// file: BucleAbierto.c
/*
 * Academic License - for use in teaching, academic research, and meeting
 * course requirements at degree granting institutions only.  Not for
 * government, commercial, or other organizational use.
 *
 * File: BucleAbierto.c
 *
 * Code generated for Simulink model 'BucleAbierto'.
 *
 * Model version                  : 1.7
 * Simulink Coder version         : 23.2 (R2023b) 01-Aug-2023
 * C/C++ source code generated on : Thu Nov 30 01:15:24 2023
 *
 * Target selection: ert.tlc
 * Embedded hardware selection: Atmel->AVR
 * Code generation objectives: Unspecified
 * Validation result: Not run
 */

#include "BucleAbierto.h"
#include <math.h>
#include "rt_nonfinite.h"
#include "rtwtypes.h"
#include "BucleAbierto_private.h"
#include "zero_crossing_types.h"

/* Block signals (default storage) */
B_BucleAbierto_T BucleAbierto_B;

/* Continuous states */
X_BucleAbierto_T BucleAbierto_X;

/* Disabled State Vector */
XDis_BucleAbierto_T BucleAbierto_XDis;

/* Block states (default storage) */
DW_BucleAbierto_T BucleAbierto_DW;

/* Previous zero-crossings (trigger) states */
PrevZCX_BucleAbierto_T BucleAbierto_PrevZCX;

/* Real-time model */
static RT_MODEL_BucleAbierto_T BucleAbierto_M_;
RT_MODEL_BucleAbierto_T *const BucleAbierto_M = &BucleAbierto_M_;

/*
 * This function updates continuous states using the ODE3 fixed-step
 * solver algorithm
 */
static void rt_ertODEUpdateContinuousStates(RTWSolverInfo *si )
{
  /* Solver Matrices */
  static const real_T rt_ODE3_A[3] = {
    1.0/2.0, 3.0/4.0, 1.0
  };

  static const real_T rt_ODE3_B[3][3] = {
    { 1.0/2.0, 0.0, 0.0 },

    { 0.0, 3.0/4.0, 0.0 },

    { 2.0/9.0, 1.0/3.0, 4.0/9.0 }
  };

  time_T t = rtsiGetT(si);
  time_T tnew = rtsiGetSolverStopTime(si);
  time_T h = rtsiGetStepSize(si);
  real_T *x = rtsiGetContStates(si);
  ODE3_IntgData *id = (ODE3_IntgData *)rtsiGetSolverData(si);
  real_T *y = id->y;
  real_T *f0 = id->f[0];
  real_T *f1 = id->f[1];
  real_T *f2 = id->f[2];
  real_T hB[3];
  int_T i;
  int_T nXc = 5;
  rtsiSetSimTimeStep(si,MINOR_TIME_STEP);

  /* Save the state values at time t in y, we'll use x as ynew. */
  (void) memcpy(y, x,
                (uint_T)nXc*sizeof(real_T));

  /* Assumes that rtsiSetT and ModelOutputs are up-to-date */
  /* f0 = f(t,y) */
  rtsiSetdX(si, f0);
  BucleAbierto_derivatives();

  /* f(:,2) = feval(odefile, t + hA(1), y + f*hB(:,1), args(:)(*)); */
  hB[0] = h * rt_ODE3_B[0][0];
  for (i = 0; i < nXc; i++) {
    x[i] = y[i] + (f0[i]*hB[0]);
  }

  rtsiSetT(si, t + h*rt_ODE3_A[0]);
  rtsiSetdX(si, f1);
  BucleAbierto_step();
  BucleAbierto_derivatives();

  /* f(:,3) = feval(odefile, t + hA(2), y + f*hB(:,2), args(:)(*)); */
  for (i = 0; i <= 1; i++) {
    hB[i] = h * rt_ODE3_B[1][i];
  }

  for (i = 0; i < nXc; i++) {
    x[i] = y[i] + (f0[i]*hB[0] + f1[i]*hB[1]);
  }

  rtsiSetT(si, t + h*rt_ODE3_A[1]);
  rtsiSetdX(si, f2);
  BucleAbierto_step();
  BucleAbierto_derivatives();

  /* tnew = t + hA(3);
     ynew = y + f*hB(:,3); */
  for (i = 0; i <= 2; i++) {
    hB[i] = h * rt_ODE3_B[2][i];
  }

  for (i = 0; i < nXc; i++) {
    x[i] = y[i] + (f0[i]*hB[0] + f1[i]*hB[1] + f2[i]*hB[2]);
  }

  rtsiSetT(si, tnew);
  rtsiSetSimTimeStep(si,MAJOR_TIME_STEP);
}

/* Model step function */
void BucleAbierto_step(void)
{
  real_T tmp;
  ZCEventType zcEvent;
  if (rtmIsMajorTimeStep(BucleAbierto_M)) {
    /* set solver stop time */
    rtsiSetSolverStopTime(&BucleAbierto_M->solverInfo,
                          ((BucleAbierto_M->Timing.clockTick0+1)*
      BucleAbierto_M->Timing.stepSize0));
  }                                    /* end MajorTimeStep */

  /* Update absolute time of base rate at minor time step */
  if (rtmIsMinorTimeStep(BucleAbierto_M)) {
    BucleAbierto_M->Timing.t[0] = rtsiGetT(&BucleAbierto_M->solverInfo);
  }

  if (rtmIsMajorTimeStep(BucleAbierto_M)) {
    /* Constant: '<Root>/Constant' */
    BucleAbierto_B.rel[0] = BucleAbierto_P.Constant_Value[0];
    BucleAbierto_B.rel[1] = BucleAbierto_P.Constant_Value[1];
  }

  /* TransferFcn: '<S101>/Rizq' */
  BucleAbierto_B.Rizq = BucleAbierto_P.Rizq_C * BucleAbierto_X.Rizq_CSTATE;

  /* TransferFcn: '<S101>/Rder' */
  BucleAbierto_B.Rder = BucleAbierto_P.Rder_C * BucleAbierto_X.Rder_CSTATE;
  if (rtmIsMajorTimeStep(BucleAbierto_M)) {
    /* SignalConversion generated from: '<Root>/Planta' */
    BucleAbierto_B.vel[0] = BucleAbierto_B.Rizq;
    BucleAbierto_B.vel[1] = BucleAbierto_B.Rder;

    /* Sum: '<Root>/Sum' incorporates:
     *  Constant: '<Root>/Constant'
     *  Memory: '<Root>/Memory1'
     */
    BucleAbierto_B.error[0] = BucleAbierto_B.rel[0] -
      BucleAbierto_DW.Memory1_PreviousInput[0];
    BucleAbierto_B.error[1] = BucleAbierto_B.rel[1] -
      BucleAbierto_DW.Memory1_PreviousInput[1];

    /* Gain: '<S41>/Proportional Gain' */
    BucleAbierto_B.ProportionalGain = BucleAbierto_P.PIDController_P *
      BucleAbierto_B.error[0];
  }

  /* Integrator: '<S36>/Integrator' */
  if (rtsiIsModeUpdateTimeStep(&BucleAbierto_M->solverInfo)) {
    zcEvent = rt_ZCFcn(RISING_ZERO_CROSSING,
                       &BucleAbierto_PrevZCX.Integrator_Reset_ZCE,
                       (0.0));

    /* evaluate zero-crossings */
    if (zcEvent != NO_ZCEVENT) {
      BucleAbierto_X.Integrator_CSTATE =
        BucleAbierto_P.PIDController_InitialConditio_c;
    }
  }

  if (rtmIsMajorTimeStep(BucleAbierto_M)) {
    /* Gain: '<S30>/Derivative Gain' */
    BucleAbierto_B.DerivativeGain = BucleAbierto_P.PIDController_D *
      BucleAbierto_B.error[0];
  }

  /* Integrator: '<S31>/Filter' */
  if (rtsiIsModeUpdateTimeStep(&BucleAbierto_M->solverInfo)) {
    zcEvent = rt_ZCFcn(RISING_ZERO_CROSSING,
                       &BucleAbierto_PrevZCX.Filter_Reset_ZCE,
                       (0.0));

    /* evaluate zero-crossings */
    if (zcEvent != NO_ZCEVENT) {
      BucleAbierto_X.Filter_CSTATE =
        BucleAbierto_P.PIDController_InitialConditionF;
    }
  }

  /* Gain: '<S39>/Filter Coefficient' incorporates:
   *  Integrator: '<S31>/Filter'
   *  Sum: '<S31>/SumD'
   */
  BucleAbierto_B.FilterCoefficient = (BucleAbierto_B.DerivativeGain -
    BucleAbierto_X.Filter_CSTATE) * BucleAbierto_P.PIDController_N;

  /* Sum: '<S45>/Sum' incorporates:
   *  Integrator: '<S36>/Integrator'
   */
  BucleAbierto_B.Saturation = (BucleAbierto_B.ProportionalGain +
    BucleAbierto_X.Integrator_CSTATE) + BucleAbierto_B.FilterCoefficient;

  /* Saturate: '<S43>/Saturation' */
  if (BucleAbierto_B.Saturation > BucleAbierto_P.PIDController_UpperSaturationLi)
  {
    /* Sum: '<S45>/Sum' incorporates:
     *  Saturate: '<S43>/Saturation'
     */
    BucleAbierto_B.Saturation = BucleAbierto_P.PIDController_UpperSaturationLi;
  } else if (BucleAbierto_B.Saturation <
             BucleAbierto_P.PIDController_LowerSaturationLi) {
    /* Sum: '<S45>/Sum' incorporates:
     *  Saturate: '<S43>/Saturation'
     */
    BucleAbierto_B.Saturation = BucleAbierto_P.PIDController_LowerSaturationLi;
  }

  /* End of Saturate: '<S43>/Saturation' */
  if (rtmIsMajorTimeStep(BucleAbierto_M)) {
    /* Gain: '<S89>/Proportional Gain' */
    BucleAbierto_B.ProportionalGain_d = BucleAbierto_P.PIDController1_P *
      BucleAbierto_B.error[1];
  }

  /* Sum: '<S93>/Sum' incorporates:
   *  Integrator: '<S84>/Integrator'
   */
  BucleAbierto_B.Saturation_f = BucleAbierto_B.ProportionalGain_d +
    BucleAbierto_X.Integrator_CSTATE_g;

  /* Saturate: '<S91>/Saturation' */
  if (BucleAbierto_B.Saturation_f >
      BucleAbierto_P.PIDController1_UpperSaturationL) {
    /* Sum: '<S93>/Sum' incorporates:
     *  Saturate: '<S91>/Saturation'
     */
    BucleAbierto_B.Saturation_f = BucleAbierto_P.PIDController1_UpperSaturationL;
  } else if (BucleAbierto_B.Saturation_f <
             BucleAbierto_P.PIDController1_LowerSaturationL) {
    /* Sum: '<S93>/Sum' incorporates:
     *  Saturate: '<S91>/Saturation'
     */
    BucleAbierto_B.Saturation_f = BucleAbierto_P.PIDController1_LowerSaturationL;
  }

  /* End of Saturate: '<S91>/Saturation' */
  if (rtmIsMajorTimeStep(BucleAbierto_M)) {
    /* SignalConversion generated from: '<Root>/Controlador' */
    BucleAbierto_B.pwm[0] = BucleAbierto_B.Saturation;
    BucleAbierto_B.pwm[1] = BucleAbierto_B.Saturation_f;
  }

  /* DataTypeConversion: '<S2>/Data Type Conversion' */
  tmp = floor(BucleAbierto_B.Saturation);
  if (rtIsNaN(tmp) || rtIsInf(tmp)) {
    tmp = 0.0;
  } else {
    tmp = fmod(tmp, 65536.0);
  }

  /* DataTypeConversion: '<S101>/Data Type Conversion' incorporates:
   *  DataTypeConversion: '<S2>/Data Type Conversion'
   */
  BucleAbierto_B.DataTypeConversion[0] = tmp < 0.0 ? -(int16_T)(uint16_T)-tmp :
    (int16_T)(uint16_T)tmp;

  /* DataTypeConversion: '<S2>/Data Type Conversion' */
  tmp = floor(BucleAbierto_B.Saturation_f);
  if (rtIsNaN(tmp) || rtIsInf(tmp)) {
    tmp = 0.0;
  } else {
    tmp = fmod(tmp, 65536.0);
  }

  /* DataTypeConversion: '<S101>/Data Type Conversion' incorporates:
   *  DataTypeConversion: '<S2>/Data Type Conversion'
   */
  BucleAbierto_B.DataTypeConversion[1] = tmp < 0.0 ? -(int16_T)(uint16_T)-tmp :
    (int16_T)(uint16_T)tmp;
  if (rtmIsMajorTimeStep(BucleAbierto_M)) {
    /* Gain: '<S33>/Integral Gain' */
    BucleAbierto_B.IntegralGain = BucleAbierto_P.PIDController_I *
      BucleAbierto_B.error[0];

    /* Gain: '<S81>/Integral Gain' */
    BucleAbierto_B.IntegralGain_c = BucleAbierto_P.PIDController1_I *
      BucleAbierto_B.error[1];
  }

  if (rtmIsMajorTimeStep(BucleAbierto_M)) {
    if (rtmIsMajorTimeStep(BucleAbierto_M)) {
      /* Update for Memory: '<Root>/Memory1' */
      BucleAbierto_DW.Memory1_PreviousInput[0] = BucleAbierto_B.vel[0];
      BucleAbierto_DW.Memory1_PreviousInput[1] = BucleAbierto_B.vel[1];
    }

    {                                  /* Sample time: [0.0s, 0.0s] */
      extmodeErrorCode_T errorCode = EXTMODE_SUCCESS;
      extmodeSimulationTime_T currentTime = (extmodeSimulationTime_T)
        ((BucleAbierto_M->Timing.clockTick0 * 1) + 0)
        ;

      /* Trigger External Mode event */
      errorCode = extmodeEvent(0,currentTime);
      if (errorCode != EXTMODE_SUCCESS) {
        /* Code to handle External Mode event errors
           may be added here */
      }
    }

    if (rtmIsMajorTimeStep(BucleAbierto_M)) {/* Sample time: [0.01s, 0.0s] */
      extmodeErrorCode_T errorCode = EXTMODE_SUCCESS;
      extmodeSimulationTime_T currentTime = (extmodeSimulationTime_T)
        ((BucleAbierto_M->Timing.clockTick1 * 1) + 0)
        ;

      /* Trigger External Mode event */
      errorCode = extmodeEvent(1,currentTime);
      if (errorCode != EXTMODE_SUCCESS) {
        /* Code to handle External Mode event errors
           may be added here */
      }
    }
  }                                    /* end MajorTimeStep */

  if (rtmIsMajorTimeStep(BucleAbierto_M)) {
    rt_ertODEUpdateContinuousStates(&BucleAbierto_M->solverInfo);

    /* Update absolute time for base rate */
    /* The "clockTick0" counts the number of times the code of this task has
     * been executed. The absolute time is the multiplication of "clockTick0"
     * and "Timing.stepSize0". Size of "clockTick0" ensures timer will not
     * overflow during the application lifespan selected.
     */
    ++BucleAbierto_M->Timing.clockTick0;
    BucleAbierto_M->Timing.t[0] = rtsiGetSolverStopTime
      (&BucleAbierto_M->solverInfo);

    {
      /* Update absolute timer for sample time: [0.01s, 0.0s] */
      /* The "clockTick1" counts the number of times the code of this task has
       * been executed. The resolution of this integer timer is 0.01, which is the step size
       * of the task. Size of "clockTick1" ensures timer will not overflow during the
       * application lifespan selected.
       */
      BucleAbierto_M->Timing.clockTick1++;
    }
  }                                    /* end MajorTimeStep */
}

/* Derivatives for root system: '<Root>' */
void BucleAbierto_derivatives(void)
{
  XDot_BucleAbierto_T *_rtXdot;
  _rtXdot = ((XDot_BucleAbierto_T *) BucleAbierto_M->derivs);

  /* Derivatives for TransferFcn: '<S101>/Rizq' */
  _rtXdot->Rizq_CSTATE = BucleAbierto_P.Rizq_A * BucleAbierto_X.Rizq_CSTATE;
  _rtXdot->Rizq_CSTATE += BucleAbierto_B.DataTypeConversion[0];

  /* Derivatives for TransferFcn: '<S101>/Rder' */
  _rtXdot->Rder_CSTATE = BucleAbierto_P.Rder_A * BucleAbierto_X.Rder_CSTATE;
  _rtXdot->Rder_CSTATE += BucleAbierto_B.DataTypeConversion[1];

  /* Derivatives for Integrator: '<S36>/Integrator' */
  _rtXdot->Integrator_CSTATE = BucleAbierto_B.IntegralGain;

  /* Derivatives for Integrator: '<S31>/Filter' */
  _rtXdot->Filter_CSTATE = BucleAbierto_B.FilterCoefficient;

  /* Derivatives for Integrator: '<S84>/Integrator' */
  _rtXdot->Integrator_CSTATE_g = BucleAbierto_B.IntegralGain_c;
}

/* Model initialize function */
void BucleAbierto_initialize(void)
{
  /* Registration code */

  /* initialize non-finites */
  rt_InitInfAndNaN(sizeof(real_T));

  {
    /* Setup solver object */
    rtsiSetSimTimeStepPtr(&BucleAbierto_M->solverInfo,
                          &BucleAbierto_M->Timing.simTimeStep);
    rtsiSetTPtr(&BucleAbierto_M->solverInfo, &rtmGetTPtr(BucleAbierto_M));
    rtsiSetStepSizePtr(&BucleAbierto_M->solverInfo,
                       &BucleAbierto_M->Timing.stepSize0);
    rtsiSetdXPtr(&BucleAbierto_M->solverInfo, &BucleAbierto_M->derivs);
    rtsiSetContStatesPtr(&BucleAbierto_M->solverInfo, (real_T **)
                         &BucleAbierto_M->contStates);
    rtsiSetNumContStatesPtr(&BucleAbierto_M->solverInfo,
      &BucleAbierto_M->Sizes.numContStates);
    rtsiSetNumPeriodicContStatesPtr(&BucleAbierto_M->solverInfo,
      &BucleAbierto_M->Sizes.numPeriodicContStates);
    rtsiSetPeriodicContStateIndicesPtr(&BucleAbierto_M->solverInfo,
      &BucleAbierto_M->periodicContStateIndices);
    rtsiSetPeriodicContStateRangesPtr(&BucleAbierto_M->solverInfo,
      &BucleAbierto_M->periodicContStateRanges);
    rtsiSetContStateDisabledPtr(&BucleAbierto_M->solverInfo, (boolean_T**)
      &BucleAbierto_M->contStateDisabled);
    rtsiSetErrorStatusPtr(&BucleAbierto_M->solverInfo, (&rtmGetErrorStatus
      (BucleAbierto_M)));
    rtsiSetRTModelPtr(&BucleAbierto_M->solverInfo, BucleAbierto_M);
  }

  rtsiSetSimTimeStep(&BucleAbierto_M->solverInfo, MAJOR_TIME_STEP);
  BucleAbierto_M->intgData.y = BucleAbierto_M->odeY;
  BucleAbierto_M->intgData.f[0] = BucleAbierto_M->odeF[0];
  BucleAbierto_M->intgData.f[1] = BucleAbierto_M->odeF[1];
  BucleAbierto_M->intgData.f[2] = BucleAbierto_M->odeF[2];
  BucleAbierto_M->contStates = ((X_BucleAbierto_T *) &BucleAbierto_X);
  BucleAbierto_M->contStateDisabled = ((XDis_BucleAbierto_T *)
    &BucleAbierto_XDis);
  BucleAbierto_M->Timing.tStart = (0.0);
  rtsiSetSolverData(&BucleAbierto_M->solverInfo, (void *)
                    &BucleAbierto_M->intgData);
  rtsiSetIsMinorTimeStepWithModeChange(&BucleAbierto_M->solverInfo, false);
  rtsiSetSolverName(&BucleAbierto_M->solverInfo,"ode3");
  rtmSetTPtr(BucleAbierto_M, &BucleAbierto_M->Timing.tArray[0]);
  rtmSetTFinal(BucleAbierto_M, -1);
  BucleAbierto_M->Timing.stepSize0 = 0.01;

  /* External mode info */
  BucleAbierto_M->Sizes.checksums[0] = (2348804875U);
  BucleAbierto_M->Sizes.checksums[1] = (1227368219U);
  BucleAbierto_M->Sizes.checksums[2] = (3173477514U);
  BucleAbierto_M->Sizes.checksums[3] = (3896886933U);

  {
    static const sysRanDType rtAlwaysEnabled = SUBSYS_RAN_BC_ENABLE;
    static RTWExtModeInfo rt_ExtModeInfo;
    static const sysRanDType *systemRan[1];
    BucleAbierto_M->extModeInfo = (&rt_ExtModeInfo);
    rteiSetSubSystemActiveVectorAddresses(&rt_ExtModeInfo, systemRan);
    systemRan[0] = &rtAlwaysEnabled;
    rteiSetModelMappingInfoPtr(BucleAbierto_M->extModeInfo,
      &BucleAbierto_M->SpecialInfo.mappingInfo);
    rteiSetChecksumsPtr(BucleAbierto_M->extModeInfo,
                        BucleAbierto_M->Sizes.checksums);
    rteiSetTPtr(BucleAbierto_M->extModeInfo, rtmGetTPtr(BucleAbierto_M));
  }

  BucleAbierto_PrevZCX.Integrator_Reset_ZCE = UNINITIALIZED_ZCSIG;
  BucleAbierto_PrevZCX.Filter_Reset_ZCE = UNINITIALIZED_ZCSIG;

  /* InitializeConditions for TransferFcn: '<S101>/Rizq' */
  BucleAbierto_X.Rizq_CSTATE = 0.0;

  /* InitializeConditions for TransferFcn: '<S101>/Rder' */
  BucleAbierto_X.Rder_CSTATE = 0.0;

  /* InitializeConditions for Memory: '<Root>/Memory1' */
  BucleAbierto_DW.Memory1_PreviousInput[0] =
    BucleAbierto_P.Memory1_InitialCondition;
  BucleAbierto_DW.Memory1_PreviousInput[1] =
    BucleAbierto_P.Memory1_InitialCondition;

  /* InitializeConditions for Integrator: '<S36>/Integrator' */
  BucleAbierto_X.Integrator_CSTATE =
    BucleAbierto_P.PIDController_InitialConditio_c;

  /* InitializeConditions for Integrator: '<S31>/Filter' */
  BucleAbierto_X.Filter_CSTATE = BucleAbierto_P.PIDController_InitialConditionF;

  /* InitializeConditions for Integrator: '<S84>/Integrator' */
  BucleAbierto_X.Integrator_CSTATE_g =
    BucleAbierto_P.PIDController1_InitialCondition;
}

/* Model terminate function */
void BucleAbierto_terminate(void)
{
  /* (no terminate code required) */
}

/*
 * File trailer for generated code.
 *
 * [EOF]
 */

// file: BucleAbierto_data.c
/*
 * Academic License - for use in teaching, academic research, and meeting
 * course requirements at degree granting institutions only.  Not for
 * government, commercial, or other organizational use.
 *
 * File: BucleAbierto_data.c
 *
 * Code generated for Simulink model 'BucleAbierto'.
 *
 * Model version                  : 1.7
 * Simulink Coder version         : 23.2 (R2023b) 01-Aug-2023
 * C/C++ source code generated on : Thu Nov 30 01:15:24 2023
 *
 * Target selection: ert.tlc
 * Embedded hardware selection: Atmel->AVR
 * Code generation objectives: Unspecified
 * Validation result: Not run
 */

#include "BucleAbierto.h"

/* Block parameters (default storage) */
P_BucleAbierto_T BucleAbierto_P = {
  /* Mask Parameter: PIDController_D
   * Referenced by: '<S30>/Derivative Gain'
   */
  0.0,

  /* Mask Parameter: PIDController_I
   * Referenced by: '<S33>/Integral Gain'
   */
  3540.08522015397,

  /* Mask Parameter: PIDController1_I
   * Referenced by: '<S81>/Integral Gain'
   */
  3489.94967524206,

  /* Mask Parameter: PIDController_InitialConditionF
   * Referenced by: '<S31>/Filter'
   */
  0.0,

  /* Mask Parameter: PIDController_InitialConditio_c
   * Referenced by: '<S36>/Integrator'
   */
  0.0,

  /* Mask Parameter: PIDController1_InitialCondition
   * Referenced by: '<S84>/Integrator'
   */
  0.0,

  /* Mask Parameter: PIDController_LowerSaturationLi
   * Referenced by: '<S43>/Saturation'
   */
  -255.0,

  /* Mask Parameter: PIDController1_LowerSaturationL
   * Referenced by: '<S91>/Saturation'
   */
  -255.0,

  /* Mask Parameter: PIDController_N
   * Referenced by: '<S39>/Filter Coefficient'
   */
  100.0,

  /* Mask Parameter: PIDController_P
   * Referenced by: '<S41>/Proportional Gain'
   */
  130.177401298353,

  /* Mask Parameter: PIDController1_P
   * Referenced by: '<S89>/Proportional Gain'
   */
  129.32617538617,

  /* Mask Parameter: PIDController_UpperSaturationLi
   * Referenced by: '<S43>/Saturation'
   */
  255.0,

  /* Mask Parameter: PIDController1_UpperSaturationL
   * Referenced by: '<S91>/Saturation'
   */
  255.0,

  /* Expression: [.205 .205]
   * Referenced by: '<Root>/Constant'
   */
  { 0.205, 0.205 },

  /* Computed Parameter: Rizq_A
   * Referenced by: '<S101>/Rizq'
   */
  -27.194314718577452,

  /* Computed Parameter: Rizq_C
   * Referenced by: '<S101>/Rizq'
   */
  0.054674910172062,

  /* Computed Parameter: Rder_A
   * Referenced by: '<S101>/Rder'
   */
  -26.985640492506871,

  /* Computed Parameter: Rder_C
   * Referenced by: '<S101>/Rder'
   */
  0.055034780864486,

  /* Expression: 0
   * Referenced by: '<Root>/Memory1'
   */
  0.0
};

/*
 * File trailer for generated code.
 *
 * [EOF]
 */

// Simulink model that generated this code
simulink model "BucleAbierto"  (R2023b)
settings: Solver=FixedStepAuto  StartTime=0.0  StopTime=inf  FixedStep=0.01  RelTol=1e-3  EnableMultiTasking=on

== system BucleAbierto ==
  Constant : Constant  Value=[.205 .205]  VectorParams1D=off
  Controlador : Subsystem  ReferencedSubsystem=Control_BCs
  Display{,1..3} (4 alike) : Display
  Memory1 : Memory
  Planta : Subsystem  ReferencedSubsystem=Piero_Beltran_23
  Scope : Scope  NumInputPorts=2
  Sum : Sum  Inputs=|+-
  wires:
  Constant/1 -> Display3/1, Scope/2, Sum/1  "rel"
  Controlador/1 -> Display1/1, Planta/1  "pwm"
  Sum/1 -> Display2/1, Controlador/1  "error"
  Planta/1 -> Memory1/1, Display/1, Scope/1  "vel."
  Memory1/1 -> Sum/2
